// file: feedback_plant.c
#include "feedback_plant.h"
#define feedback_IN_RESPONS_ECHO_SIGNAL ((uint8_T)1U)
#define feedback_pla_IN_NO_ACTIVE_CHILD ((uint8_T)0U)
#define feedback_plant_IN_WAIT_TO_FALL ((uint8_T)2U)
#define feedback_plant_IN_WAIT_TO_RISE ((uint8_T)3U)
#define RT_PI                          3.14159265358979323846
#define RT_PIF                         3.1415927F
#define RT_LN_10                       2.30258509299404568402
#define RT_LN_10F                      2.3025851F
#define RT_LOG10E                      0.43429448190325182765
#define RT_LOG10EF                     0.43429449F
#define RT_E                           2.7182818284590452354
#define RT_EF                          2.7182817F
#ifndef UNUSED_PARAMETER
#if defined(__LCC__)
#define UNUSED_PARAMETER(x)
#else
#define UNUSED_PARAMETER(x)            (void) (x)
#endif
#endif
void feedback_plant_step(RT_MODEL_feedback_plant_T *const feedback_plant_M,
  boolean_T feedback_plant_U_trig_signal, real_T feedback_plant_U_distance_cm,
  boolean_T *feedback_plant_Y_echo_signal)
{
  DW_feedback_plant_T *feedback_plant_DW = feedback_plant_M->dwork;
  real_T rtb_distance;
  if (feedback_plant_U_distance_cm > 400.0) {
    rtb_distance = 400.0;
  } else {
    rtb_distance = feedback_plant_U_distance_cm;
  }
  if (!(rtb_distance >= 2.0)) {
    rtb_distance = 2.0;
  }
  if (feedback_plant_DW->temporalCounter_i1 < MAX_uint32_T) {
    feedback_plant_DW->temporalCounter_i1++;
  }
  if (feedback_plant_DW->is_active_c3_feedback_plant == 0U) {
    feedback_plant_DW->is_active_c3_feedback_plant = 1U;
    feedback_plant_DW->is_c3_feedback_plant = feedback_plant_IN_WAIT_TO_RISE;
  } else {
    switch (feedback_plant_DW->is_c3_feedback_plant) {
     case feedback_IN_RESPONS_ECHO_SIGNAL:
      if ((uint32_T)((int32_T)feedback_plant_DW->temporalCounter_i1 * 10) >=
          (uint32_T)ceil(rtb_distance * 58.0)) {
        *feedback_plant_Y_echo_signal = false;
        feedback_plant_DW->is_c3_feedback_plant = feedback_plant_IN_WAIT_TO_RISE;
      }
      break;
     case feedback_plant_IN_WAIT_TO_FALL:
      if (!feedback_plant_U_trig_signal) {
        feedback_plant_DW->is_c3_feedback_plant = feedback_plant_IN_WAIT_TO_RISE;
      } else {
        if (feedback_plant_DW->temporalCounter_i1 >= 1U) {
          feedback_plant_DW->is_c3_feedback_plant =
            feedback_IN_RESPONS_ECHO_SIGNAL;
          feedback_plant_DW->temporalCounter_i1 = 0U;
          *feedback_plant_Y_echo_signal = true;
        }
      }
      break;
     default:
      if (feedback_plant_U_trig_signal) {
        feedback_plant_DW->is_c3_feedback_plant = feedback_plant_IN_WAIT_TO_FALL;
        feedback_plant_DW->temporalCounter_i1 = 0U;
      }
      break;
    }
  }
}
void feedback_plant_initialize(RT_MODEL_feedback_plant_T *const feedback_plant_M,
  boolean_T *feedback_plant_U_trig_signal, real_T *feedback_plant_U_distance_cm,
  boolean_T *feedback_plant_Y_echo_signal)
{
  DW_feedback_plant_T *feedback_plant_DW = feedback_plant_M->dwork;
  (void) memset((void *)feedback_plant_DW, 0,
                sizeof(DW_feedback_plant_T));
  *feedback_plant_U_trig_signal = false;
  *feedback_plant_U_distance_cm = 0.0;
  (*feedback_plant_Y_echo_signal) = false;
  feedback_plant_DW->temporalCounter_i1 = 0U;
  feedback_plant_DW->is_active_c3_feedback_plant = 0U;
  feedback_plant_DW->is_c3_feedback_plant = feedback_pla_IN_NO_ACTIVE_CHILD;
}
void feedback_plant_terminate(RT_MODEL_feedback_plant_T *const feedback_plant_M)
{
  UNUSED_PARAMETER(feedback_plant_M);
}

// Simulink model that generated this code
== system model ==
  trig_signal : Inport
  distance_cm : Inport
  echo_signal : Outport  <- 1: Stateflowchart#1
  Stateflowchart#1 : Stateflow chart  <- 1: trig_signal, 2: Product#1
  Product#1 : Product  <- 1: Switch#1, 2: Constant#1
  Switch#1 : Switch  Threshold=2  <- 1: Switch#2, 2: Switch#2, 3: Constant#2
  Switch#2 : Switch  Criteria=u2 > Threshold  Threshold=400  <- 1: Constant#3, 2: distance_cm, 3: distance_cm
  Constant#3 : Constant  Value=400
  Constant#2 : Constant  Value=2
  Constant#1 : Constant  Value=58
== stateflow chart Stateflowchart#1 ==
  state WAIT_TO_RISE
  state WAIT_TO_FALL
  state RESPONS_ECHO_SIGNAL
    entry:
    echo_signal = true;
    exit:
    echo_signal = false;
  (default) -> WAIT_TO_RISE
  (junction 16) -> WAIT_TO_RISE
  (junction 22) -> (junction 16)
  WAIT_TO_RISE -> WAIT_TO_FALL : [trig_signal == true]
  WAIT_TO_FALL -> (junction 22) [order 1] : [trig_signal == false]
  (junction 14) -> (junction 22)
  WAIT_TO_FALL -> RESPONS_ECHO_SIGNAL [order 2] : [after(10,usec)]
  RESPONS_ECHO_SIGNAL -> (junction 14) : after(echo_pulse_duration_us, usec)
  data: trig_signal input boolean; echo_pulse_duration_us input double; echo_signal output boolean
